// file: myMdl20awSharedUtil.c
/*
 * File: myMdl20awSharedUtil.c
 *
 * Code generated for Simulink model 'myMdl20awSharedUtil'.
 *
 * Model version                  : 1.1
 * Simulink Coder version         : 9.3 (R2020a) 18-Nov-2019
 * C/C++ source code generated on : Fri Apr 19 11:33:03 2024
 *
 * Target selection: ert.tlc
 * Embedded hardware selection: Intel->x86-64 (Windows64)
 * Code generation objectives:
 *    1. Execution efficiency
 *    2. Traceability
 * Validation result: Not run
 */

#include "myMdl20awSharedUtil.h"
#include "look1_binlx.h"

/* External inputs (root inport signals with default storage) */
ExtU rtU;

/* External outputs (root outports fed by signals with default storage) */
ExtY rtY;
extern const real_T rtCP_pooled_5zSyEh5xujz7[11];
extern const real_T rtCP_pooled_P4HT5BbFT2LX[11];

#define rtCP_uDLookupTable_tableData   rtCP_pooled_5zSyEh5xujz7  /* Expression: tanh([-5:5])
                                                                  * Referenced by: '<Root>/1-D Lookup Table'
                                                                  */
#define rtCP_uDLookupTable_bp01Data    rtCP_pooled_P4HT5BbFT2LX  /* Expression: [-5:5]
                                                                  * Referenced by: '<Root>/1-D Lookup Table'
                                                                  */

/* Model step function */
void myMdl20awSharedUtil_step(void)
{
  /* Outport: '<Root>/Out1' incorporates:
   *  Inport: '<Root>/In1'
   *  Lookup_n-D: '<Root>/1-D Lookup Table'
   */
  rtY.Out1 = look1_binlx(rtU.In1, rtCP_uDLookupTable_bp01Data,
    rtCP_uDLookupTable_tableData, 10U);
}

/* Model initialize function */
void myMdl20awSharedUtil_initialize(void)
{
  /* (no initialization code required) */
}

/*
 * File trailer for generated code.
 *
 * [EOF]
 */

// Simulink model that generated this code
simulink model "myMdl20awSharedUtil"  (R2020a)
settings: Solver=FixedStepDiscrete  StartTime=0.0  StopTime=10.0  RelTol=1e-3
model workspace (MATLAB code in the model file):
  | cmdLim = Simulink.Parameter;
  | cmdLim.Value = 15;
  | cmdLim.Description = 'Limit for controlling the maximum surface command angle.';
  | cmdLim.Min = 0;
  | cmdLim.Max = 90;
  | cmdLim.DocUnits = 'deg';
  | 
  | dispGain = Simulink.Parameter;
  | dispGain.Value = 0.75;
  | dispGain.Description = 'Gain applied to the displacement error.';
  | dispGain.Min = 0;
  | dispGain.Max = [];
  | dispGain.DocUnits = 'deg/sec/deg';
  | 
  | dispLim = Simulink.Parameter;
  | dispLim.Value = 30;
  | dispLim.Description = 'Limit for controlling the maximum commanded angle.';
  | dispLim.Min = 0;
  | dispLim.Max = 180;
  | dispLim.DocUnits = 'deg';
  | 
  | intGain = Simulink.Parameter;
  | intGain.Value = 0.5;
  | intGain.Description = 'Gain applied to the integral error.';
  | intGain.Min = 0;
  | intGain.Max = [];
  | intGain.DocUnits = 'deg/sec/deg/sec';
  | 
  | intLim = Simulink.Parameter;
  | intLim.Value = 5;
  | intLim.Description = 'Limit for controlling the maximum commanded angle.';
  | intLim.Min = 0;
  | intLim.Max = 90;
  | intLim.DocUnits = 'deg';
  | 
  | rateGain = Simulink.Parameter;
  | rateGain.Value = 2;
  | rateGain.Description = 'Gain applied to the rate error.';
  | rateGain.Min = 0;
  | rateGain.Max = [];
  | rateGain.DocUnits = 'deg/deg/sec';
  | 
  | rateLim = Simulink.Parameter;
  | rateLim.Value = 6;
  | rateLim.Description = 'Limit for controlling the maximum commanded angle.';
  | rateLim.Min = 0;
  | rateLim.Max = 180;
  | rateLim.DocUnits = 'deg/sec';
  | 
  | hdgGain = Simulink.Parameter;
  | hdgGain.Value = 0.015;

== system myMdl20awSharedUtil ==
  In1 : Inport
  1-D Lookup Table : Lookup_n-D  NumberOfTableDimensions=1  BreakpointsForDimension1=[-5:5]  Table=tanh([-5:5])  InternalRulePriority=Speed  RndMeth=Simplest  InputSameDT=on
  Out1 : Outport
  wires:
  In1/1 -> 1-D Lookup Table/1
  1-D Lookup Table/1 -> Out1/1
